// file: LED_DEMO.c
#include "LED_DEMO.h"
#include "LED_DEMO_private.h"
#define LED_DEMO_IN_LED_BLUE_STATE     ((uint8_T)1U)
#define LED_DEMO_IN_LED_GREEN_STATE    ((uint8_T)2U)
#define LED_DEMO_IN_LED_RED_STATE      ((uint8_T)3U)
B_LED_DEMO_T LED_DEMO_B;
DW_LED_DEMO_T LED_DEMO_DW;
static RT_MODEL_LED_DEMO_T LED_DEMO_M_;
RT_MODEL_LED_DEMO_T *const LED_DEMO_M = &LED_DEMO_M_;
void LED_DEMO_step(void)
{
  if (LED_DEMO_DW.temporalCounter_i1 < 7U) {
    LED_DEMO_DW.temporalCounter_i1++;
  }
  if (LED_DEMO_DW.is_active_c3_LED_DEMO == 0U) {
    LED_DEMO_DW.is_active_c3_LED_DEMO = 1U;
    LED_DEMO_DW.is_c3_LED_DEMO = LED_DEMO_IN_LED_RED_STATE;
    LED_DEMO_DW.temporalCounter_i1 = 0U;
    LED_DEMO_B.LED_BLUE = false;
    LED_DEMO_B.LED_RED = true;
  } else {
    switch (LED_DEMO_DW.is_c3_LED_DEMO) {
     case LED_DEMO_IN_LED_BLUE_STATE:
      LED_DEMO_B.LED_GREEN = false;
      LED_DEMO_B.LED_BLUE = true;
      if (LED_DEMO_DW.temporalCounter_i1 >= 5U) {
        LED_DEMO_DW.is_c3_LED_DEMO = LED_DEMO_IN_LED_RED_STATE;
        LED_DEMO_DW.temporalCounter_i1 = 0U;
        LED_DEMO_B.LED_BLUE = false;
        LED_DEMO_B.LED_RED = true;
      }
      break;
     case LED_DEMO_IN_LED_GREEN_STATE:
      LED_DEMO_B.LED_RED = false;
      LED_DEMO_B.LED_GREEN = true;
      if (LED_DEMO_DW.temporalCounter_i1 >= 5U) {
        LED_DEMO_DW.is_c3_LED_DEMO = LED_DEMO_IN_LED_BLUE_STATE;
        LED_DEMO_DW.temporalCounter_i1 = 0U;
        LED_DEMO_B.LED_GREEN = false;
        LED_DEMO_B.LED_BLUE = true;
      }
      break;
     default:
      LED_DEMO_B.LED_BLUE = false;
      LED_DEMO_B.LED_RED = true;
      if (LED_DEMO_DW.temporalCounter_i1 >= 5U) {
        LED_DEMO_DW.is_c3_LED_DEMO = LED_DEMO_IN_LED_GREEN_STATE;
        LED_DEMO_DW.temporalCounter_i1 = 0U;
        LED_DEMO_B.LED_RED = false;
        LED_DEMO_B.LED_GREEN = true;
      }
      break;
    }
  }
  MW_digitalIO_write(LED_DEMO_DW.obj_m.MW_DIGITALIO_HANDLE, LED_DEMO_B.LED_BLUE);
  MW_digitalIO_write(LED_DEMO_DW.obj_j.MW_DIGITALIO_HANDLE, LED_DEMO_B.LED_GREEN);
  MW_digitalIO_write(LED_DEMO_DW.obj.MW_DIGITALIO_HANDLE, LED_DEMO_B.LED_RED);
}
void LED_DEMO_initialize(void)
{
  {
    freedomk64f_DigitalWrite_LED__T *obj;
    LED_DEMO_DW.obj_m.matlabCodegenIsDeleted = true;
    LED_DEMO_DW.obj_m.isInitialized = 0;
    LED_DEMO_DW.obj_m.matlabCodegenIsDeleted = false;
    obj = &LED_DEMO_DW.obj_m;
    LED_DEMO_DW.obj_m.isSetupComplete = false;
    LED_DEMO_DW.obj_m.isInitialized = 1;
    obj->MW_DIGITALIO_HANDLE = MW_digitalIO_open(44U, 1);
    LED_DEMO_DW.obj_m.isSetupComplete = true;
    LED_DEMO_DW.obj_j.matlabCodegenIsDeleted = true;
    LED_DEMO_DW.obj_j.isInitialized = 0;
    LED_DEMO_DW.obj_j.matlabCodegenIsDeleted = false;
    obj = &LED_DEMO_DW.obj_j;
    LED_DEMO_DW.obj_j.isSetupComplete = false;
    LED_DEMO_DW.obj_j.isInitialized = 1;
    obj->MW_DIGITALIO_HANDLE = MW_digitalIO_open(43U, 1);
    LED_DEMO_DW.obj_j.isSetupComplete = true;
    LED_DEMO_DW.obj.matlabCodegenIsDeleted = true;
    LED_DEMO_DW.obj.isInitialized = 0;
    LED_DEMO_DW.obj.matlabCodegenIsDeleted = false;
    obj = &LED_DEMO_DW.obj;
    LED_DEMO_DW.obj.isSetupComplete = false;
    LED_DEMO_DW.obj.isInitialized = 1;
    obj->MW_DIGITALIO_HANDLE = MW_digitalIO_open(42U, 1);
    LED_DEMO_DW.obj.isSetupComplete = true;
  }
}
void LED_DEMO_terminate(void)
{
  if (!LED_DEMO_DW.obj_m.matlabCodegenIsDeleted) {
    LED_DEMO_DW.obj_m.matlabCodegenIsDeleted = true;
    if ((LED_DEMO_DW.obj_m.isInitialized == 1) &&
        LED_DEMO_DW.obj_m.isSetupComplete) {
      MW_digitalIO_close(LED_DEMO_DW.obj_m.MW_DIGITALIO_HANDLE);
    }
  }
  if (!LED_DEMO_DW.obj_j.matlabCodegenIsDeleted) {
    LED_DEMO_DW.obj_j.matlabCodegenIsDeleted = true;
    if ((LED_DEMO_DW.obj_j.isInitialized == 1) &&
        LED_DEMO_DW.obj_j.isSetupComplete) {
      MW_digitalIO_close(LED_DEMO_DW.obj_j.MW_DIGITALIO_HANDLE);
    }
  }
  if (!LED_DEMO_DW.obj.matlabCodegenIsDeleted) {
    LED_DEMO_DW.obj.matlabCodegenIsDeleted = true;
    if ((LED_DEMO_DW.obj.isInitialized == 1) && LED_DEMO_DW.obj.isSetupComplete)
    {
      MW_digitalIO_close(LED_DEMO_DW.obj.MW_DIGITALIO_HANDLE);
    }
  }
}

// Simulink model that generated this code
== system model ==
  LED_BLUE : frdmk64flib/Digital Write  <- 1: Stateflowchart#1/3
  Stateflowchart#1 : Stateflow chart
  LED_GREEN : frdmk64flib/Digital Write  <- 1: Stateflowchart#1/2
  LED_RED : frdmk64flib/Digital Write  <- 1: Stateflowchart#1
== stateflow chart Stateflowchart#1 ==
  state LED_RED_STATE
    entry:
    LED_BLUE = false;
    LED_RED = true;
  state LED_GREEN_STATE
    entry:
    LED_RED = false;
    LED_GREEN = true;
  state LED_BLUE_STATE
    entry:
    LED_GREEN = false;
    LED_BLUE = true;
  (default) -> LED_RED_STATE
  LED_RED_STATE -> LED_GREEN_STATE : after(5,msec)
  LED_BLUE_STATE -> LED_RED_STATE : after(5,msec)
  LED_GREEN_STATE -> LED_BLUE_STATE : after(5,msec)
  data: LED_RED output boolean; LED_GREEN output boolean; LED_BLUE output boolean
